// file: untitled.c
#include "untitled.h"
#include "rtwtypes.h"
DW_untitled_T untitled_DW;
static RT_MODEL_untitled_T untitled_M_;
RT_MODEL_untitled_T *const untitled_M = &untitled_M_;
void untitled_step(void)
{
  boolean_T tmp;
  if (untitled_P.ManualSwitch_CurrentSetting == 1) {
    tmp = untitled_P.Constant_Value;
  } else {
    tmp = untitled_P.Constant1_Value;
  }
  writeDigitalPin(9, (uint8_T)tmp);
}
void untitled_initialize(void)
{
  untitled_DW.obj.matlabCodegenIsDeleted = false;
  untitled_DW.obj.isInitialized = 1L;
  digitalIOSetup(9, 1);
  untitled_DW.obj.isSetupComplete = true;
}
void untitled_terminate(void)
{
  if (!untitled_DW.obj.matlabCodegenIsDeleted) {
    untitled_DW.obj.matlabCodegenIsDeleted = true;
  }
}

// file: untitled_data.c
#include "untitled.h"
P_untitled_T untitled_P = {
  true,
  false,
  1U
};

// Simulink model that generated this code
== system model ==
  DigitalOutput#1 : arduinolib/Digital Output  pinNumber=9  <- 1: ManualSwitch
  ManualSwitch : ManualSwitch  <- 1: Constant, 2: Constant1
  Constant : Constant
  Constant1 : Constant  Value=0
